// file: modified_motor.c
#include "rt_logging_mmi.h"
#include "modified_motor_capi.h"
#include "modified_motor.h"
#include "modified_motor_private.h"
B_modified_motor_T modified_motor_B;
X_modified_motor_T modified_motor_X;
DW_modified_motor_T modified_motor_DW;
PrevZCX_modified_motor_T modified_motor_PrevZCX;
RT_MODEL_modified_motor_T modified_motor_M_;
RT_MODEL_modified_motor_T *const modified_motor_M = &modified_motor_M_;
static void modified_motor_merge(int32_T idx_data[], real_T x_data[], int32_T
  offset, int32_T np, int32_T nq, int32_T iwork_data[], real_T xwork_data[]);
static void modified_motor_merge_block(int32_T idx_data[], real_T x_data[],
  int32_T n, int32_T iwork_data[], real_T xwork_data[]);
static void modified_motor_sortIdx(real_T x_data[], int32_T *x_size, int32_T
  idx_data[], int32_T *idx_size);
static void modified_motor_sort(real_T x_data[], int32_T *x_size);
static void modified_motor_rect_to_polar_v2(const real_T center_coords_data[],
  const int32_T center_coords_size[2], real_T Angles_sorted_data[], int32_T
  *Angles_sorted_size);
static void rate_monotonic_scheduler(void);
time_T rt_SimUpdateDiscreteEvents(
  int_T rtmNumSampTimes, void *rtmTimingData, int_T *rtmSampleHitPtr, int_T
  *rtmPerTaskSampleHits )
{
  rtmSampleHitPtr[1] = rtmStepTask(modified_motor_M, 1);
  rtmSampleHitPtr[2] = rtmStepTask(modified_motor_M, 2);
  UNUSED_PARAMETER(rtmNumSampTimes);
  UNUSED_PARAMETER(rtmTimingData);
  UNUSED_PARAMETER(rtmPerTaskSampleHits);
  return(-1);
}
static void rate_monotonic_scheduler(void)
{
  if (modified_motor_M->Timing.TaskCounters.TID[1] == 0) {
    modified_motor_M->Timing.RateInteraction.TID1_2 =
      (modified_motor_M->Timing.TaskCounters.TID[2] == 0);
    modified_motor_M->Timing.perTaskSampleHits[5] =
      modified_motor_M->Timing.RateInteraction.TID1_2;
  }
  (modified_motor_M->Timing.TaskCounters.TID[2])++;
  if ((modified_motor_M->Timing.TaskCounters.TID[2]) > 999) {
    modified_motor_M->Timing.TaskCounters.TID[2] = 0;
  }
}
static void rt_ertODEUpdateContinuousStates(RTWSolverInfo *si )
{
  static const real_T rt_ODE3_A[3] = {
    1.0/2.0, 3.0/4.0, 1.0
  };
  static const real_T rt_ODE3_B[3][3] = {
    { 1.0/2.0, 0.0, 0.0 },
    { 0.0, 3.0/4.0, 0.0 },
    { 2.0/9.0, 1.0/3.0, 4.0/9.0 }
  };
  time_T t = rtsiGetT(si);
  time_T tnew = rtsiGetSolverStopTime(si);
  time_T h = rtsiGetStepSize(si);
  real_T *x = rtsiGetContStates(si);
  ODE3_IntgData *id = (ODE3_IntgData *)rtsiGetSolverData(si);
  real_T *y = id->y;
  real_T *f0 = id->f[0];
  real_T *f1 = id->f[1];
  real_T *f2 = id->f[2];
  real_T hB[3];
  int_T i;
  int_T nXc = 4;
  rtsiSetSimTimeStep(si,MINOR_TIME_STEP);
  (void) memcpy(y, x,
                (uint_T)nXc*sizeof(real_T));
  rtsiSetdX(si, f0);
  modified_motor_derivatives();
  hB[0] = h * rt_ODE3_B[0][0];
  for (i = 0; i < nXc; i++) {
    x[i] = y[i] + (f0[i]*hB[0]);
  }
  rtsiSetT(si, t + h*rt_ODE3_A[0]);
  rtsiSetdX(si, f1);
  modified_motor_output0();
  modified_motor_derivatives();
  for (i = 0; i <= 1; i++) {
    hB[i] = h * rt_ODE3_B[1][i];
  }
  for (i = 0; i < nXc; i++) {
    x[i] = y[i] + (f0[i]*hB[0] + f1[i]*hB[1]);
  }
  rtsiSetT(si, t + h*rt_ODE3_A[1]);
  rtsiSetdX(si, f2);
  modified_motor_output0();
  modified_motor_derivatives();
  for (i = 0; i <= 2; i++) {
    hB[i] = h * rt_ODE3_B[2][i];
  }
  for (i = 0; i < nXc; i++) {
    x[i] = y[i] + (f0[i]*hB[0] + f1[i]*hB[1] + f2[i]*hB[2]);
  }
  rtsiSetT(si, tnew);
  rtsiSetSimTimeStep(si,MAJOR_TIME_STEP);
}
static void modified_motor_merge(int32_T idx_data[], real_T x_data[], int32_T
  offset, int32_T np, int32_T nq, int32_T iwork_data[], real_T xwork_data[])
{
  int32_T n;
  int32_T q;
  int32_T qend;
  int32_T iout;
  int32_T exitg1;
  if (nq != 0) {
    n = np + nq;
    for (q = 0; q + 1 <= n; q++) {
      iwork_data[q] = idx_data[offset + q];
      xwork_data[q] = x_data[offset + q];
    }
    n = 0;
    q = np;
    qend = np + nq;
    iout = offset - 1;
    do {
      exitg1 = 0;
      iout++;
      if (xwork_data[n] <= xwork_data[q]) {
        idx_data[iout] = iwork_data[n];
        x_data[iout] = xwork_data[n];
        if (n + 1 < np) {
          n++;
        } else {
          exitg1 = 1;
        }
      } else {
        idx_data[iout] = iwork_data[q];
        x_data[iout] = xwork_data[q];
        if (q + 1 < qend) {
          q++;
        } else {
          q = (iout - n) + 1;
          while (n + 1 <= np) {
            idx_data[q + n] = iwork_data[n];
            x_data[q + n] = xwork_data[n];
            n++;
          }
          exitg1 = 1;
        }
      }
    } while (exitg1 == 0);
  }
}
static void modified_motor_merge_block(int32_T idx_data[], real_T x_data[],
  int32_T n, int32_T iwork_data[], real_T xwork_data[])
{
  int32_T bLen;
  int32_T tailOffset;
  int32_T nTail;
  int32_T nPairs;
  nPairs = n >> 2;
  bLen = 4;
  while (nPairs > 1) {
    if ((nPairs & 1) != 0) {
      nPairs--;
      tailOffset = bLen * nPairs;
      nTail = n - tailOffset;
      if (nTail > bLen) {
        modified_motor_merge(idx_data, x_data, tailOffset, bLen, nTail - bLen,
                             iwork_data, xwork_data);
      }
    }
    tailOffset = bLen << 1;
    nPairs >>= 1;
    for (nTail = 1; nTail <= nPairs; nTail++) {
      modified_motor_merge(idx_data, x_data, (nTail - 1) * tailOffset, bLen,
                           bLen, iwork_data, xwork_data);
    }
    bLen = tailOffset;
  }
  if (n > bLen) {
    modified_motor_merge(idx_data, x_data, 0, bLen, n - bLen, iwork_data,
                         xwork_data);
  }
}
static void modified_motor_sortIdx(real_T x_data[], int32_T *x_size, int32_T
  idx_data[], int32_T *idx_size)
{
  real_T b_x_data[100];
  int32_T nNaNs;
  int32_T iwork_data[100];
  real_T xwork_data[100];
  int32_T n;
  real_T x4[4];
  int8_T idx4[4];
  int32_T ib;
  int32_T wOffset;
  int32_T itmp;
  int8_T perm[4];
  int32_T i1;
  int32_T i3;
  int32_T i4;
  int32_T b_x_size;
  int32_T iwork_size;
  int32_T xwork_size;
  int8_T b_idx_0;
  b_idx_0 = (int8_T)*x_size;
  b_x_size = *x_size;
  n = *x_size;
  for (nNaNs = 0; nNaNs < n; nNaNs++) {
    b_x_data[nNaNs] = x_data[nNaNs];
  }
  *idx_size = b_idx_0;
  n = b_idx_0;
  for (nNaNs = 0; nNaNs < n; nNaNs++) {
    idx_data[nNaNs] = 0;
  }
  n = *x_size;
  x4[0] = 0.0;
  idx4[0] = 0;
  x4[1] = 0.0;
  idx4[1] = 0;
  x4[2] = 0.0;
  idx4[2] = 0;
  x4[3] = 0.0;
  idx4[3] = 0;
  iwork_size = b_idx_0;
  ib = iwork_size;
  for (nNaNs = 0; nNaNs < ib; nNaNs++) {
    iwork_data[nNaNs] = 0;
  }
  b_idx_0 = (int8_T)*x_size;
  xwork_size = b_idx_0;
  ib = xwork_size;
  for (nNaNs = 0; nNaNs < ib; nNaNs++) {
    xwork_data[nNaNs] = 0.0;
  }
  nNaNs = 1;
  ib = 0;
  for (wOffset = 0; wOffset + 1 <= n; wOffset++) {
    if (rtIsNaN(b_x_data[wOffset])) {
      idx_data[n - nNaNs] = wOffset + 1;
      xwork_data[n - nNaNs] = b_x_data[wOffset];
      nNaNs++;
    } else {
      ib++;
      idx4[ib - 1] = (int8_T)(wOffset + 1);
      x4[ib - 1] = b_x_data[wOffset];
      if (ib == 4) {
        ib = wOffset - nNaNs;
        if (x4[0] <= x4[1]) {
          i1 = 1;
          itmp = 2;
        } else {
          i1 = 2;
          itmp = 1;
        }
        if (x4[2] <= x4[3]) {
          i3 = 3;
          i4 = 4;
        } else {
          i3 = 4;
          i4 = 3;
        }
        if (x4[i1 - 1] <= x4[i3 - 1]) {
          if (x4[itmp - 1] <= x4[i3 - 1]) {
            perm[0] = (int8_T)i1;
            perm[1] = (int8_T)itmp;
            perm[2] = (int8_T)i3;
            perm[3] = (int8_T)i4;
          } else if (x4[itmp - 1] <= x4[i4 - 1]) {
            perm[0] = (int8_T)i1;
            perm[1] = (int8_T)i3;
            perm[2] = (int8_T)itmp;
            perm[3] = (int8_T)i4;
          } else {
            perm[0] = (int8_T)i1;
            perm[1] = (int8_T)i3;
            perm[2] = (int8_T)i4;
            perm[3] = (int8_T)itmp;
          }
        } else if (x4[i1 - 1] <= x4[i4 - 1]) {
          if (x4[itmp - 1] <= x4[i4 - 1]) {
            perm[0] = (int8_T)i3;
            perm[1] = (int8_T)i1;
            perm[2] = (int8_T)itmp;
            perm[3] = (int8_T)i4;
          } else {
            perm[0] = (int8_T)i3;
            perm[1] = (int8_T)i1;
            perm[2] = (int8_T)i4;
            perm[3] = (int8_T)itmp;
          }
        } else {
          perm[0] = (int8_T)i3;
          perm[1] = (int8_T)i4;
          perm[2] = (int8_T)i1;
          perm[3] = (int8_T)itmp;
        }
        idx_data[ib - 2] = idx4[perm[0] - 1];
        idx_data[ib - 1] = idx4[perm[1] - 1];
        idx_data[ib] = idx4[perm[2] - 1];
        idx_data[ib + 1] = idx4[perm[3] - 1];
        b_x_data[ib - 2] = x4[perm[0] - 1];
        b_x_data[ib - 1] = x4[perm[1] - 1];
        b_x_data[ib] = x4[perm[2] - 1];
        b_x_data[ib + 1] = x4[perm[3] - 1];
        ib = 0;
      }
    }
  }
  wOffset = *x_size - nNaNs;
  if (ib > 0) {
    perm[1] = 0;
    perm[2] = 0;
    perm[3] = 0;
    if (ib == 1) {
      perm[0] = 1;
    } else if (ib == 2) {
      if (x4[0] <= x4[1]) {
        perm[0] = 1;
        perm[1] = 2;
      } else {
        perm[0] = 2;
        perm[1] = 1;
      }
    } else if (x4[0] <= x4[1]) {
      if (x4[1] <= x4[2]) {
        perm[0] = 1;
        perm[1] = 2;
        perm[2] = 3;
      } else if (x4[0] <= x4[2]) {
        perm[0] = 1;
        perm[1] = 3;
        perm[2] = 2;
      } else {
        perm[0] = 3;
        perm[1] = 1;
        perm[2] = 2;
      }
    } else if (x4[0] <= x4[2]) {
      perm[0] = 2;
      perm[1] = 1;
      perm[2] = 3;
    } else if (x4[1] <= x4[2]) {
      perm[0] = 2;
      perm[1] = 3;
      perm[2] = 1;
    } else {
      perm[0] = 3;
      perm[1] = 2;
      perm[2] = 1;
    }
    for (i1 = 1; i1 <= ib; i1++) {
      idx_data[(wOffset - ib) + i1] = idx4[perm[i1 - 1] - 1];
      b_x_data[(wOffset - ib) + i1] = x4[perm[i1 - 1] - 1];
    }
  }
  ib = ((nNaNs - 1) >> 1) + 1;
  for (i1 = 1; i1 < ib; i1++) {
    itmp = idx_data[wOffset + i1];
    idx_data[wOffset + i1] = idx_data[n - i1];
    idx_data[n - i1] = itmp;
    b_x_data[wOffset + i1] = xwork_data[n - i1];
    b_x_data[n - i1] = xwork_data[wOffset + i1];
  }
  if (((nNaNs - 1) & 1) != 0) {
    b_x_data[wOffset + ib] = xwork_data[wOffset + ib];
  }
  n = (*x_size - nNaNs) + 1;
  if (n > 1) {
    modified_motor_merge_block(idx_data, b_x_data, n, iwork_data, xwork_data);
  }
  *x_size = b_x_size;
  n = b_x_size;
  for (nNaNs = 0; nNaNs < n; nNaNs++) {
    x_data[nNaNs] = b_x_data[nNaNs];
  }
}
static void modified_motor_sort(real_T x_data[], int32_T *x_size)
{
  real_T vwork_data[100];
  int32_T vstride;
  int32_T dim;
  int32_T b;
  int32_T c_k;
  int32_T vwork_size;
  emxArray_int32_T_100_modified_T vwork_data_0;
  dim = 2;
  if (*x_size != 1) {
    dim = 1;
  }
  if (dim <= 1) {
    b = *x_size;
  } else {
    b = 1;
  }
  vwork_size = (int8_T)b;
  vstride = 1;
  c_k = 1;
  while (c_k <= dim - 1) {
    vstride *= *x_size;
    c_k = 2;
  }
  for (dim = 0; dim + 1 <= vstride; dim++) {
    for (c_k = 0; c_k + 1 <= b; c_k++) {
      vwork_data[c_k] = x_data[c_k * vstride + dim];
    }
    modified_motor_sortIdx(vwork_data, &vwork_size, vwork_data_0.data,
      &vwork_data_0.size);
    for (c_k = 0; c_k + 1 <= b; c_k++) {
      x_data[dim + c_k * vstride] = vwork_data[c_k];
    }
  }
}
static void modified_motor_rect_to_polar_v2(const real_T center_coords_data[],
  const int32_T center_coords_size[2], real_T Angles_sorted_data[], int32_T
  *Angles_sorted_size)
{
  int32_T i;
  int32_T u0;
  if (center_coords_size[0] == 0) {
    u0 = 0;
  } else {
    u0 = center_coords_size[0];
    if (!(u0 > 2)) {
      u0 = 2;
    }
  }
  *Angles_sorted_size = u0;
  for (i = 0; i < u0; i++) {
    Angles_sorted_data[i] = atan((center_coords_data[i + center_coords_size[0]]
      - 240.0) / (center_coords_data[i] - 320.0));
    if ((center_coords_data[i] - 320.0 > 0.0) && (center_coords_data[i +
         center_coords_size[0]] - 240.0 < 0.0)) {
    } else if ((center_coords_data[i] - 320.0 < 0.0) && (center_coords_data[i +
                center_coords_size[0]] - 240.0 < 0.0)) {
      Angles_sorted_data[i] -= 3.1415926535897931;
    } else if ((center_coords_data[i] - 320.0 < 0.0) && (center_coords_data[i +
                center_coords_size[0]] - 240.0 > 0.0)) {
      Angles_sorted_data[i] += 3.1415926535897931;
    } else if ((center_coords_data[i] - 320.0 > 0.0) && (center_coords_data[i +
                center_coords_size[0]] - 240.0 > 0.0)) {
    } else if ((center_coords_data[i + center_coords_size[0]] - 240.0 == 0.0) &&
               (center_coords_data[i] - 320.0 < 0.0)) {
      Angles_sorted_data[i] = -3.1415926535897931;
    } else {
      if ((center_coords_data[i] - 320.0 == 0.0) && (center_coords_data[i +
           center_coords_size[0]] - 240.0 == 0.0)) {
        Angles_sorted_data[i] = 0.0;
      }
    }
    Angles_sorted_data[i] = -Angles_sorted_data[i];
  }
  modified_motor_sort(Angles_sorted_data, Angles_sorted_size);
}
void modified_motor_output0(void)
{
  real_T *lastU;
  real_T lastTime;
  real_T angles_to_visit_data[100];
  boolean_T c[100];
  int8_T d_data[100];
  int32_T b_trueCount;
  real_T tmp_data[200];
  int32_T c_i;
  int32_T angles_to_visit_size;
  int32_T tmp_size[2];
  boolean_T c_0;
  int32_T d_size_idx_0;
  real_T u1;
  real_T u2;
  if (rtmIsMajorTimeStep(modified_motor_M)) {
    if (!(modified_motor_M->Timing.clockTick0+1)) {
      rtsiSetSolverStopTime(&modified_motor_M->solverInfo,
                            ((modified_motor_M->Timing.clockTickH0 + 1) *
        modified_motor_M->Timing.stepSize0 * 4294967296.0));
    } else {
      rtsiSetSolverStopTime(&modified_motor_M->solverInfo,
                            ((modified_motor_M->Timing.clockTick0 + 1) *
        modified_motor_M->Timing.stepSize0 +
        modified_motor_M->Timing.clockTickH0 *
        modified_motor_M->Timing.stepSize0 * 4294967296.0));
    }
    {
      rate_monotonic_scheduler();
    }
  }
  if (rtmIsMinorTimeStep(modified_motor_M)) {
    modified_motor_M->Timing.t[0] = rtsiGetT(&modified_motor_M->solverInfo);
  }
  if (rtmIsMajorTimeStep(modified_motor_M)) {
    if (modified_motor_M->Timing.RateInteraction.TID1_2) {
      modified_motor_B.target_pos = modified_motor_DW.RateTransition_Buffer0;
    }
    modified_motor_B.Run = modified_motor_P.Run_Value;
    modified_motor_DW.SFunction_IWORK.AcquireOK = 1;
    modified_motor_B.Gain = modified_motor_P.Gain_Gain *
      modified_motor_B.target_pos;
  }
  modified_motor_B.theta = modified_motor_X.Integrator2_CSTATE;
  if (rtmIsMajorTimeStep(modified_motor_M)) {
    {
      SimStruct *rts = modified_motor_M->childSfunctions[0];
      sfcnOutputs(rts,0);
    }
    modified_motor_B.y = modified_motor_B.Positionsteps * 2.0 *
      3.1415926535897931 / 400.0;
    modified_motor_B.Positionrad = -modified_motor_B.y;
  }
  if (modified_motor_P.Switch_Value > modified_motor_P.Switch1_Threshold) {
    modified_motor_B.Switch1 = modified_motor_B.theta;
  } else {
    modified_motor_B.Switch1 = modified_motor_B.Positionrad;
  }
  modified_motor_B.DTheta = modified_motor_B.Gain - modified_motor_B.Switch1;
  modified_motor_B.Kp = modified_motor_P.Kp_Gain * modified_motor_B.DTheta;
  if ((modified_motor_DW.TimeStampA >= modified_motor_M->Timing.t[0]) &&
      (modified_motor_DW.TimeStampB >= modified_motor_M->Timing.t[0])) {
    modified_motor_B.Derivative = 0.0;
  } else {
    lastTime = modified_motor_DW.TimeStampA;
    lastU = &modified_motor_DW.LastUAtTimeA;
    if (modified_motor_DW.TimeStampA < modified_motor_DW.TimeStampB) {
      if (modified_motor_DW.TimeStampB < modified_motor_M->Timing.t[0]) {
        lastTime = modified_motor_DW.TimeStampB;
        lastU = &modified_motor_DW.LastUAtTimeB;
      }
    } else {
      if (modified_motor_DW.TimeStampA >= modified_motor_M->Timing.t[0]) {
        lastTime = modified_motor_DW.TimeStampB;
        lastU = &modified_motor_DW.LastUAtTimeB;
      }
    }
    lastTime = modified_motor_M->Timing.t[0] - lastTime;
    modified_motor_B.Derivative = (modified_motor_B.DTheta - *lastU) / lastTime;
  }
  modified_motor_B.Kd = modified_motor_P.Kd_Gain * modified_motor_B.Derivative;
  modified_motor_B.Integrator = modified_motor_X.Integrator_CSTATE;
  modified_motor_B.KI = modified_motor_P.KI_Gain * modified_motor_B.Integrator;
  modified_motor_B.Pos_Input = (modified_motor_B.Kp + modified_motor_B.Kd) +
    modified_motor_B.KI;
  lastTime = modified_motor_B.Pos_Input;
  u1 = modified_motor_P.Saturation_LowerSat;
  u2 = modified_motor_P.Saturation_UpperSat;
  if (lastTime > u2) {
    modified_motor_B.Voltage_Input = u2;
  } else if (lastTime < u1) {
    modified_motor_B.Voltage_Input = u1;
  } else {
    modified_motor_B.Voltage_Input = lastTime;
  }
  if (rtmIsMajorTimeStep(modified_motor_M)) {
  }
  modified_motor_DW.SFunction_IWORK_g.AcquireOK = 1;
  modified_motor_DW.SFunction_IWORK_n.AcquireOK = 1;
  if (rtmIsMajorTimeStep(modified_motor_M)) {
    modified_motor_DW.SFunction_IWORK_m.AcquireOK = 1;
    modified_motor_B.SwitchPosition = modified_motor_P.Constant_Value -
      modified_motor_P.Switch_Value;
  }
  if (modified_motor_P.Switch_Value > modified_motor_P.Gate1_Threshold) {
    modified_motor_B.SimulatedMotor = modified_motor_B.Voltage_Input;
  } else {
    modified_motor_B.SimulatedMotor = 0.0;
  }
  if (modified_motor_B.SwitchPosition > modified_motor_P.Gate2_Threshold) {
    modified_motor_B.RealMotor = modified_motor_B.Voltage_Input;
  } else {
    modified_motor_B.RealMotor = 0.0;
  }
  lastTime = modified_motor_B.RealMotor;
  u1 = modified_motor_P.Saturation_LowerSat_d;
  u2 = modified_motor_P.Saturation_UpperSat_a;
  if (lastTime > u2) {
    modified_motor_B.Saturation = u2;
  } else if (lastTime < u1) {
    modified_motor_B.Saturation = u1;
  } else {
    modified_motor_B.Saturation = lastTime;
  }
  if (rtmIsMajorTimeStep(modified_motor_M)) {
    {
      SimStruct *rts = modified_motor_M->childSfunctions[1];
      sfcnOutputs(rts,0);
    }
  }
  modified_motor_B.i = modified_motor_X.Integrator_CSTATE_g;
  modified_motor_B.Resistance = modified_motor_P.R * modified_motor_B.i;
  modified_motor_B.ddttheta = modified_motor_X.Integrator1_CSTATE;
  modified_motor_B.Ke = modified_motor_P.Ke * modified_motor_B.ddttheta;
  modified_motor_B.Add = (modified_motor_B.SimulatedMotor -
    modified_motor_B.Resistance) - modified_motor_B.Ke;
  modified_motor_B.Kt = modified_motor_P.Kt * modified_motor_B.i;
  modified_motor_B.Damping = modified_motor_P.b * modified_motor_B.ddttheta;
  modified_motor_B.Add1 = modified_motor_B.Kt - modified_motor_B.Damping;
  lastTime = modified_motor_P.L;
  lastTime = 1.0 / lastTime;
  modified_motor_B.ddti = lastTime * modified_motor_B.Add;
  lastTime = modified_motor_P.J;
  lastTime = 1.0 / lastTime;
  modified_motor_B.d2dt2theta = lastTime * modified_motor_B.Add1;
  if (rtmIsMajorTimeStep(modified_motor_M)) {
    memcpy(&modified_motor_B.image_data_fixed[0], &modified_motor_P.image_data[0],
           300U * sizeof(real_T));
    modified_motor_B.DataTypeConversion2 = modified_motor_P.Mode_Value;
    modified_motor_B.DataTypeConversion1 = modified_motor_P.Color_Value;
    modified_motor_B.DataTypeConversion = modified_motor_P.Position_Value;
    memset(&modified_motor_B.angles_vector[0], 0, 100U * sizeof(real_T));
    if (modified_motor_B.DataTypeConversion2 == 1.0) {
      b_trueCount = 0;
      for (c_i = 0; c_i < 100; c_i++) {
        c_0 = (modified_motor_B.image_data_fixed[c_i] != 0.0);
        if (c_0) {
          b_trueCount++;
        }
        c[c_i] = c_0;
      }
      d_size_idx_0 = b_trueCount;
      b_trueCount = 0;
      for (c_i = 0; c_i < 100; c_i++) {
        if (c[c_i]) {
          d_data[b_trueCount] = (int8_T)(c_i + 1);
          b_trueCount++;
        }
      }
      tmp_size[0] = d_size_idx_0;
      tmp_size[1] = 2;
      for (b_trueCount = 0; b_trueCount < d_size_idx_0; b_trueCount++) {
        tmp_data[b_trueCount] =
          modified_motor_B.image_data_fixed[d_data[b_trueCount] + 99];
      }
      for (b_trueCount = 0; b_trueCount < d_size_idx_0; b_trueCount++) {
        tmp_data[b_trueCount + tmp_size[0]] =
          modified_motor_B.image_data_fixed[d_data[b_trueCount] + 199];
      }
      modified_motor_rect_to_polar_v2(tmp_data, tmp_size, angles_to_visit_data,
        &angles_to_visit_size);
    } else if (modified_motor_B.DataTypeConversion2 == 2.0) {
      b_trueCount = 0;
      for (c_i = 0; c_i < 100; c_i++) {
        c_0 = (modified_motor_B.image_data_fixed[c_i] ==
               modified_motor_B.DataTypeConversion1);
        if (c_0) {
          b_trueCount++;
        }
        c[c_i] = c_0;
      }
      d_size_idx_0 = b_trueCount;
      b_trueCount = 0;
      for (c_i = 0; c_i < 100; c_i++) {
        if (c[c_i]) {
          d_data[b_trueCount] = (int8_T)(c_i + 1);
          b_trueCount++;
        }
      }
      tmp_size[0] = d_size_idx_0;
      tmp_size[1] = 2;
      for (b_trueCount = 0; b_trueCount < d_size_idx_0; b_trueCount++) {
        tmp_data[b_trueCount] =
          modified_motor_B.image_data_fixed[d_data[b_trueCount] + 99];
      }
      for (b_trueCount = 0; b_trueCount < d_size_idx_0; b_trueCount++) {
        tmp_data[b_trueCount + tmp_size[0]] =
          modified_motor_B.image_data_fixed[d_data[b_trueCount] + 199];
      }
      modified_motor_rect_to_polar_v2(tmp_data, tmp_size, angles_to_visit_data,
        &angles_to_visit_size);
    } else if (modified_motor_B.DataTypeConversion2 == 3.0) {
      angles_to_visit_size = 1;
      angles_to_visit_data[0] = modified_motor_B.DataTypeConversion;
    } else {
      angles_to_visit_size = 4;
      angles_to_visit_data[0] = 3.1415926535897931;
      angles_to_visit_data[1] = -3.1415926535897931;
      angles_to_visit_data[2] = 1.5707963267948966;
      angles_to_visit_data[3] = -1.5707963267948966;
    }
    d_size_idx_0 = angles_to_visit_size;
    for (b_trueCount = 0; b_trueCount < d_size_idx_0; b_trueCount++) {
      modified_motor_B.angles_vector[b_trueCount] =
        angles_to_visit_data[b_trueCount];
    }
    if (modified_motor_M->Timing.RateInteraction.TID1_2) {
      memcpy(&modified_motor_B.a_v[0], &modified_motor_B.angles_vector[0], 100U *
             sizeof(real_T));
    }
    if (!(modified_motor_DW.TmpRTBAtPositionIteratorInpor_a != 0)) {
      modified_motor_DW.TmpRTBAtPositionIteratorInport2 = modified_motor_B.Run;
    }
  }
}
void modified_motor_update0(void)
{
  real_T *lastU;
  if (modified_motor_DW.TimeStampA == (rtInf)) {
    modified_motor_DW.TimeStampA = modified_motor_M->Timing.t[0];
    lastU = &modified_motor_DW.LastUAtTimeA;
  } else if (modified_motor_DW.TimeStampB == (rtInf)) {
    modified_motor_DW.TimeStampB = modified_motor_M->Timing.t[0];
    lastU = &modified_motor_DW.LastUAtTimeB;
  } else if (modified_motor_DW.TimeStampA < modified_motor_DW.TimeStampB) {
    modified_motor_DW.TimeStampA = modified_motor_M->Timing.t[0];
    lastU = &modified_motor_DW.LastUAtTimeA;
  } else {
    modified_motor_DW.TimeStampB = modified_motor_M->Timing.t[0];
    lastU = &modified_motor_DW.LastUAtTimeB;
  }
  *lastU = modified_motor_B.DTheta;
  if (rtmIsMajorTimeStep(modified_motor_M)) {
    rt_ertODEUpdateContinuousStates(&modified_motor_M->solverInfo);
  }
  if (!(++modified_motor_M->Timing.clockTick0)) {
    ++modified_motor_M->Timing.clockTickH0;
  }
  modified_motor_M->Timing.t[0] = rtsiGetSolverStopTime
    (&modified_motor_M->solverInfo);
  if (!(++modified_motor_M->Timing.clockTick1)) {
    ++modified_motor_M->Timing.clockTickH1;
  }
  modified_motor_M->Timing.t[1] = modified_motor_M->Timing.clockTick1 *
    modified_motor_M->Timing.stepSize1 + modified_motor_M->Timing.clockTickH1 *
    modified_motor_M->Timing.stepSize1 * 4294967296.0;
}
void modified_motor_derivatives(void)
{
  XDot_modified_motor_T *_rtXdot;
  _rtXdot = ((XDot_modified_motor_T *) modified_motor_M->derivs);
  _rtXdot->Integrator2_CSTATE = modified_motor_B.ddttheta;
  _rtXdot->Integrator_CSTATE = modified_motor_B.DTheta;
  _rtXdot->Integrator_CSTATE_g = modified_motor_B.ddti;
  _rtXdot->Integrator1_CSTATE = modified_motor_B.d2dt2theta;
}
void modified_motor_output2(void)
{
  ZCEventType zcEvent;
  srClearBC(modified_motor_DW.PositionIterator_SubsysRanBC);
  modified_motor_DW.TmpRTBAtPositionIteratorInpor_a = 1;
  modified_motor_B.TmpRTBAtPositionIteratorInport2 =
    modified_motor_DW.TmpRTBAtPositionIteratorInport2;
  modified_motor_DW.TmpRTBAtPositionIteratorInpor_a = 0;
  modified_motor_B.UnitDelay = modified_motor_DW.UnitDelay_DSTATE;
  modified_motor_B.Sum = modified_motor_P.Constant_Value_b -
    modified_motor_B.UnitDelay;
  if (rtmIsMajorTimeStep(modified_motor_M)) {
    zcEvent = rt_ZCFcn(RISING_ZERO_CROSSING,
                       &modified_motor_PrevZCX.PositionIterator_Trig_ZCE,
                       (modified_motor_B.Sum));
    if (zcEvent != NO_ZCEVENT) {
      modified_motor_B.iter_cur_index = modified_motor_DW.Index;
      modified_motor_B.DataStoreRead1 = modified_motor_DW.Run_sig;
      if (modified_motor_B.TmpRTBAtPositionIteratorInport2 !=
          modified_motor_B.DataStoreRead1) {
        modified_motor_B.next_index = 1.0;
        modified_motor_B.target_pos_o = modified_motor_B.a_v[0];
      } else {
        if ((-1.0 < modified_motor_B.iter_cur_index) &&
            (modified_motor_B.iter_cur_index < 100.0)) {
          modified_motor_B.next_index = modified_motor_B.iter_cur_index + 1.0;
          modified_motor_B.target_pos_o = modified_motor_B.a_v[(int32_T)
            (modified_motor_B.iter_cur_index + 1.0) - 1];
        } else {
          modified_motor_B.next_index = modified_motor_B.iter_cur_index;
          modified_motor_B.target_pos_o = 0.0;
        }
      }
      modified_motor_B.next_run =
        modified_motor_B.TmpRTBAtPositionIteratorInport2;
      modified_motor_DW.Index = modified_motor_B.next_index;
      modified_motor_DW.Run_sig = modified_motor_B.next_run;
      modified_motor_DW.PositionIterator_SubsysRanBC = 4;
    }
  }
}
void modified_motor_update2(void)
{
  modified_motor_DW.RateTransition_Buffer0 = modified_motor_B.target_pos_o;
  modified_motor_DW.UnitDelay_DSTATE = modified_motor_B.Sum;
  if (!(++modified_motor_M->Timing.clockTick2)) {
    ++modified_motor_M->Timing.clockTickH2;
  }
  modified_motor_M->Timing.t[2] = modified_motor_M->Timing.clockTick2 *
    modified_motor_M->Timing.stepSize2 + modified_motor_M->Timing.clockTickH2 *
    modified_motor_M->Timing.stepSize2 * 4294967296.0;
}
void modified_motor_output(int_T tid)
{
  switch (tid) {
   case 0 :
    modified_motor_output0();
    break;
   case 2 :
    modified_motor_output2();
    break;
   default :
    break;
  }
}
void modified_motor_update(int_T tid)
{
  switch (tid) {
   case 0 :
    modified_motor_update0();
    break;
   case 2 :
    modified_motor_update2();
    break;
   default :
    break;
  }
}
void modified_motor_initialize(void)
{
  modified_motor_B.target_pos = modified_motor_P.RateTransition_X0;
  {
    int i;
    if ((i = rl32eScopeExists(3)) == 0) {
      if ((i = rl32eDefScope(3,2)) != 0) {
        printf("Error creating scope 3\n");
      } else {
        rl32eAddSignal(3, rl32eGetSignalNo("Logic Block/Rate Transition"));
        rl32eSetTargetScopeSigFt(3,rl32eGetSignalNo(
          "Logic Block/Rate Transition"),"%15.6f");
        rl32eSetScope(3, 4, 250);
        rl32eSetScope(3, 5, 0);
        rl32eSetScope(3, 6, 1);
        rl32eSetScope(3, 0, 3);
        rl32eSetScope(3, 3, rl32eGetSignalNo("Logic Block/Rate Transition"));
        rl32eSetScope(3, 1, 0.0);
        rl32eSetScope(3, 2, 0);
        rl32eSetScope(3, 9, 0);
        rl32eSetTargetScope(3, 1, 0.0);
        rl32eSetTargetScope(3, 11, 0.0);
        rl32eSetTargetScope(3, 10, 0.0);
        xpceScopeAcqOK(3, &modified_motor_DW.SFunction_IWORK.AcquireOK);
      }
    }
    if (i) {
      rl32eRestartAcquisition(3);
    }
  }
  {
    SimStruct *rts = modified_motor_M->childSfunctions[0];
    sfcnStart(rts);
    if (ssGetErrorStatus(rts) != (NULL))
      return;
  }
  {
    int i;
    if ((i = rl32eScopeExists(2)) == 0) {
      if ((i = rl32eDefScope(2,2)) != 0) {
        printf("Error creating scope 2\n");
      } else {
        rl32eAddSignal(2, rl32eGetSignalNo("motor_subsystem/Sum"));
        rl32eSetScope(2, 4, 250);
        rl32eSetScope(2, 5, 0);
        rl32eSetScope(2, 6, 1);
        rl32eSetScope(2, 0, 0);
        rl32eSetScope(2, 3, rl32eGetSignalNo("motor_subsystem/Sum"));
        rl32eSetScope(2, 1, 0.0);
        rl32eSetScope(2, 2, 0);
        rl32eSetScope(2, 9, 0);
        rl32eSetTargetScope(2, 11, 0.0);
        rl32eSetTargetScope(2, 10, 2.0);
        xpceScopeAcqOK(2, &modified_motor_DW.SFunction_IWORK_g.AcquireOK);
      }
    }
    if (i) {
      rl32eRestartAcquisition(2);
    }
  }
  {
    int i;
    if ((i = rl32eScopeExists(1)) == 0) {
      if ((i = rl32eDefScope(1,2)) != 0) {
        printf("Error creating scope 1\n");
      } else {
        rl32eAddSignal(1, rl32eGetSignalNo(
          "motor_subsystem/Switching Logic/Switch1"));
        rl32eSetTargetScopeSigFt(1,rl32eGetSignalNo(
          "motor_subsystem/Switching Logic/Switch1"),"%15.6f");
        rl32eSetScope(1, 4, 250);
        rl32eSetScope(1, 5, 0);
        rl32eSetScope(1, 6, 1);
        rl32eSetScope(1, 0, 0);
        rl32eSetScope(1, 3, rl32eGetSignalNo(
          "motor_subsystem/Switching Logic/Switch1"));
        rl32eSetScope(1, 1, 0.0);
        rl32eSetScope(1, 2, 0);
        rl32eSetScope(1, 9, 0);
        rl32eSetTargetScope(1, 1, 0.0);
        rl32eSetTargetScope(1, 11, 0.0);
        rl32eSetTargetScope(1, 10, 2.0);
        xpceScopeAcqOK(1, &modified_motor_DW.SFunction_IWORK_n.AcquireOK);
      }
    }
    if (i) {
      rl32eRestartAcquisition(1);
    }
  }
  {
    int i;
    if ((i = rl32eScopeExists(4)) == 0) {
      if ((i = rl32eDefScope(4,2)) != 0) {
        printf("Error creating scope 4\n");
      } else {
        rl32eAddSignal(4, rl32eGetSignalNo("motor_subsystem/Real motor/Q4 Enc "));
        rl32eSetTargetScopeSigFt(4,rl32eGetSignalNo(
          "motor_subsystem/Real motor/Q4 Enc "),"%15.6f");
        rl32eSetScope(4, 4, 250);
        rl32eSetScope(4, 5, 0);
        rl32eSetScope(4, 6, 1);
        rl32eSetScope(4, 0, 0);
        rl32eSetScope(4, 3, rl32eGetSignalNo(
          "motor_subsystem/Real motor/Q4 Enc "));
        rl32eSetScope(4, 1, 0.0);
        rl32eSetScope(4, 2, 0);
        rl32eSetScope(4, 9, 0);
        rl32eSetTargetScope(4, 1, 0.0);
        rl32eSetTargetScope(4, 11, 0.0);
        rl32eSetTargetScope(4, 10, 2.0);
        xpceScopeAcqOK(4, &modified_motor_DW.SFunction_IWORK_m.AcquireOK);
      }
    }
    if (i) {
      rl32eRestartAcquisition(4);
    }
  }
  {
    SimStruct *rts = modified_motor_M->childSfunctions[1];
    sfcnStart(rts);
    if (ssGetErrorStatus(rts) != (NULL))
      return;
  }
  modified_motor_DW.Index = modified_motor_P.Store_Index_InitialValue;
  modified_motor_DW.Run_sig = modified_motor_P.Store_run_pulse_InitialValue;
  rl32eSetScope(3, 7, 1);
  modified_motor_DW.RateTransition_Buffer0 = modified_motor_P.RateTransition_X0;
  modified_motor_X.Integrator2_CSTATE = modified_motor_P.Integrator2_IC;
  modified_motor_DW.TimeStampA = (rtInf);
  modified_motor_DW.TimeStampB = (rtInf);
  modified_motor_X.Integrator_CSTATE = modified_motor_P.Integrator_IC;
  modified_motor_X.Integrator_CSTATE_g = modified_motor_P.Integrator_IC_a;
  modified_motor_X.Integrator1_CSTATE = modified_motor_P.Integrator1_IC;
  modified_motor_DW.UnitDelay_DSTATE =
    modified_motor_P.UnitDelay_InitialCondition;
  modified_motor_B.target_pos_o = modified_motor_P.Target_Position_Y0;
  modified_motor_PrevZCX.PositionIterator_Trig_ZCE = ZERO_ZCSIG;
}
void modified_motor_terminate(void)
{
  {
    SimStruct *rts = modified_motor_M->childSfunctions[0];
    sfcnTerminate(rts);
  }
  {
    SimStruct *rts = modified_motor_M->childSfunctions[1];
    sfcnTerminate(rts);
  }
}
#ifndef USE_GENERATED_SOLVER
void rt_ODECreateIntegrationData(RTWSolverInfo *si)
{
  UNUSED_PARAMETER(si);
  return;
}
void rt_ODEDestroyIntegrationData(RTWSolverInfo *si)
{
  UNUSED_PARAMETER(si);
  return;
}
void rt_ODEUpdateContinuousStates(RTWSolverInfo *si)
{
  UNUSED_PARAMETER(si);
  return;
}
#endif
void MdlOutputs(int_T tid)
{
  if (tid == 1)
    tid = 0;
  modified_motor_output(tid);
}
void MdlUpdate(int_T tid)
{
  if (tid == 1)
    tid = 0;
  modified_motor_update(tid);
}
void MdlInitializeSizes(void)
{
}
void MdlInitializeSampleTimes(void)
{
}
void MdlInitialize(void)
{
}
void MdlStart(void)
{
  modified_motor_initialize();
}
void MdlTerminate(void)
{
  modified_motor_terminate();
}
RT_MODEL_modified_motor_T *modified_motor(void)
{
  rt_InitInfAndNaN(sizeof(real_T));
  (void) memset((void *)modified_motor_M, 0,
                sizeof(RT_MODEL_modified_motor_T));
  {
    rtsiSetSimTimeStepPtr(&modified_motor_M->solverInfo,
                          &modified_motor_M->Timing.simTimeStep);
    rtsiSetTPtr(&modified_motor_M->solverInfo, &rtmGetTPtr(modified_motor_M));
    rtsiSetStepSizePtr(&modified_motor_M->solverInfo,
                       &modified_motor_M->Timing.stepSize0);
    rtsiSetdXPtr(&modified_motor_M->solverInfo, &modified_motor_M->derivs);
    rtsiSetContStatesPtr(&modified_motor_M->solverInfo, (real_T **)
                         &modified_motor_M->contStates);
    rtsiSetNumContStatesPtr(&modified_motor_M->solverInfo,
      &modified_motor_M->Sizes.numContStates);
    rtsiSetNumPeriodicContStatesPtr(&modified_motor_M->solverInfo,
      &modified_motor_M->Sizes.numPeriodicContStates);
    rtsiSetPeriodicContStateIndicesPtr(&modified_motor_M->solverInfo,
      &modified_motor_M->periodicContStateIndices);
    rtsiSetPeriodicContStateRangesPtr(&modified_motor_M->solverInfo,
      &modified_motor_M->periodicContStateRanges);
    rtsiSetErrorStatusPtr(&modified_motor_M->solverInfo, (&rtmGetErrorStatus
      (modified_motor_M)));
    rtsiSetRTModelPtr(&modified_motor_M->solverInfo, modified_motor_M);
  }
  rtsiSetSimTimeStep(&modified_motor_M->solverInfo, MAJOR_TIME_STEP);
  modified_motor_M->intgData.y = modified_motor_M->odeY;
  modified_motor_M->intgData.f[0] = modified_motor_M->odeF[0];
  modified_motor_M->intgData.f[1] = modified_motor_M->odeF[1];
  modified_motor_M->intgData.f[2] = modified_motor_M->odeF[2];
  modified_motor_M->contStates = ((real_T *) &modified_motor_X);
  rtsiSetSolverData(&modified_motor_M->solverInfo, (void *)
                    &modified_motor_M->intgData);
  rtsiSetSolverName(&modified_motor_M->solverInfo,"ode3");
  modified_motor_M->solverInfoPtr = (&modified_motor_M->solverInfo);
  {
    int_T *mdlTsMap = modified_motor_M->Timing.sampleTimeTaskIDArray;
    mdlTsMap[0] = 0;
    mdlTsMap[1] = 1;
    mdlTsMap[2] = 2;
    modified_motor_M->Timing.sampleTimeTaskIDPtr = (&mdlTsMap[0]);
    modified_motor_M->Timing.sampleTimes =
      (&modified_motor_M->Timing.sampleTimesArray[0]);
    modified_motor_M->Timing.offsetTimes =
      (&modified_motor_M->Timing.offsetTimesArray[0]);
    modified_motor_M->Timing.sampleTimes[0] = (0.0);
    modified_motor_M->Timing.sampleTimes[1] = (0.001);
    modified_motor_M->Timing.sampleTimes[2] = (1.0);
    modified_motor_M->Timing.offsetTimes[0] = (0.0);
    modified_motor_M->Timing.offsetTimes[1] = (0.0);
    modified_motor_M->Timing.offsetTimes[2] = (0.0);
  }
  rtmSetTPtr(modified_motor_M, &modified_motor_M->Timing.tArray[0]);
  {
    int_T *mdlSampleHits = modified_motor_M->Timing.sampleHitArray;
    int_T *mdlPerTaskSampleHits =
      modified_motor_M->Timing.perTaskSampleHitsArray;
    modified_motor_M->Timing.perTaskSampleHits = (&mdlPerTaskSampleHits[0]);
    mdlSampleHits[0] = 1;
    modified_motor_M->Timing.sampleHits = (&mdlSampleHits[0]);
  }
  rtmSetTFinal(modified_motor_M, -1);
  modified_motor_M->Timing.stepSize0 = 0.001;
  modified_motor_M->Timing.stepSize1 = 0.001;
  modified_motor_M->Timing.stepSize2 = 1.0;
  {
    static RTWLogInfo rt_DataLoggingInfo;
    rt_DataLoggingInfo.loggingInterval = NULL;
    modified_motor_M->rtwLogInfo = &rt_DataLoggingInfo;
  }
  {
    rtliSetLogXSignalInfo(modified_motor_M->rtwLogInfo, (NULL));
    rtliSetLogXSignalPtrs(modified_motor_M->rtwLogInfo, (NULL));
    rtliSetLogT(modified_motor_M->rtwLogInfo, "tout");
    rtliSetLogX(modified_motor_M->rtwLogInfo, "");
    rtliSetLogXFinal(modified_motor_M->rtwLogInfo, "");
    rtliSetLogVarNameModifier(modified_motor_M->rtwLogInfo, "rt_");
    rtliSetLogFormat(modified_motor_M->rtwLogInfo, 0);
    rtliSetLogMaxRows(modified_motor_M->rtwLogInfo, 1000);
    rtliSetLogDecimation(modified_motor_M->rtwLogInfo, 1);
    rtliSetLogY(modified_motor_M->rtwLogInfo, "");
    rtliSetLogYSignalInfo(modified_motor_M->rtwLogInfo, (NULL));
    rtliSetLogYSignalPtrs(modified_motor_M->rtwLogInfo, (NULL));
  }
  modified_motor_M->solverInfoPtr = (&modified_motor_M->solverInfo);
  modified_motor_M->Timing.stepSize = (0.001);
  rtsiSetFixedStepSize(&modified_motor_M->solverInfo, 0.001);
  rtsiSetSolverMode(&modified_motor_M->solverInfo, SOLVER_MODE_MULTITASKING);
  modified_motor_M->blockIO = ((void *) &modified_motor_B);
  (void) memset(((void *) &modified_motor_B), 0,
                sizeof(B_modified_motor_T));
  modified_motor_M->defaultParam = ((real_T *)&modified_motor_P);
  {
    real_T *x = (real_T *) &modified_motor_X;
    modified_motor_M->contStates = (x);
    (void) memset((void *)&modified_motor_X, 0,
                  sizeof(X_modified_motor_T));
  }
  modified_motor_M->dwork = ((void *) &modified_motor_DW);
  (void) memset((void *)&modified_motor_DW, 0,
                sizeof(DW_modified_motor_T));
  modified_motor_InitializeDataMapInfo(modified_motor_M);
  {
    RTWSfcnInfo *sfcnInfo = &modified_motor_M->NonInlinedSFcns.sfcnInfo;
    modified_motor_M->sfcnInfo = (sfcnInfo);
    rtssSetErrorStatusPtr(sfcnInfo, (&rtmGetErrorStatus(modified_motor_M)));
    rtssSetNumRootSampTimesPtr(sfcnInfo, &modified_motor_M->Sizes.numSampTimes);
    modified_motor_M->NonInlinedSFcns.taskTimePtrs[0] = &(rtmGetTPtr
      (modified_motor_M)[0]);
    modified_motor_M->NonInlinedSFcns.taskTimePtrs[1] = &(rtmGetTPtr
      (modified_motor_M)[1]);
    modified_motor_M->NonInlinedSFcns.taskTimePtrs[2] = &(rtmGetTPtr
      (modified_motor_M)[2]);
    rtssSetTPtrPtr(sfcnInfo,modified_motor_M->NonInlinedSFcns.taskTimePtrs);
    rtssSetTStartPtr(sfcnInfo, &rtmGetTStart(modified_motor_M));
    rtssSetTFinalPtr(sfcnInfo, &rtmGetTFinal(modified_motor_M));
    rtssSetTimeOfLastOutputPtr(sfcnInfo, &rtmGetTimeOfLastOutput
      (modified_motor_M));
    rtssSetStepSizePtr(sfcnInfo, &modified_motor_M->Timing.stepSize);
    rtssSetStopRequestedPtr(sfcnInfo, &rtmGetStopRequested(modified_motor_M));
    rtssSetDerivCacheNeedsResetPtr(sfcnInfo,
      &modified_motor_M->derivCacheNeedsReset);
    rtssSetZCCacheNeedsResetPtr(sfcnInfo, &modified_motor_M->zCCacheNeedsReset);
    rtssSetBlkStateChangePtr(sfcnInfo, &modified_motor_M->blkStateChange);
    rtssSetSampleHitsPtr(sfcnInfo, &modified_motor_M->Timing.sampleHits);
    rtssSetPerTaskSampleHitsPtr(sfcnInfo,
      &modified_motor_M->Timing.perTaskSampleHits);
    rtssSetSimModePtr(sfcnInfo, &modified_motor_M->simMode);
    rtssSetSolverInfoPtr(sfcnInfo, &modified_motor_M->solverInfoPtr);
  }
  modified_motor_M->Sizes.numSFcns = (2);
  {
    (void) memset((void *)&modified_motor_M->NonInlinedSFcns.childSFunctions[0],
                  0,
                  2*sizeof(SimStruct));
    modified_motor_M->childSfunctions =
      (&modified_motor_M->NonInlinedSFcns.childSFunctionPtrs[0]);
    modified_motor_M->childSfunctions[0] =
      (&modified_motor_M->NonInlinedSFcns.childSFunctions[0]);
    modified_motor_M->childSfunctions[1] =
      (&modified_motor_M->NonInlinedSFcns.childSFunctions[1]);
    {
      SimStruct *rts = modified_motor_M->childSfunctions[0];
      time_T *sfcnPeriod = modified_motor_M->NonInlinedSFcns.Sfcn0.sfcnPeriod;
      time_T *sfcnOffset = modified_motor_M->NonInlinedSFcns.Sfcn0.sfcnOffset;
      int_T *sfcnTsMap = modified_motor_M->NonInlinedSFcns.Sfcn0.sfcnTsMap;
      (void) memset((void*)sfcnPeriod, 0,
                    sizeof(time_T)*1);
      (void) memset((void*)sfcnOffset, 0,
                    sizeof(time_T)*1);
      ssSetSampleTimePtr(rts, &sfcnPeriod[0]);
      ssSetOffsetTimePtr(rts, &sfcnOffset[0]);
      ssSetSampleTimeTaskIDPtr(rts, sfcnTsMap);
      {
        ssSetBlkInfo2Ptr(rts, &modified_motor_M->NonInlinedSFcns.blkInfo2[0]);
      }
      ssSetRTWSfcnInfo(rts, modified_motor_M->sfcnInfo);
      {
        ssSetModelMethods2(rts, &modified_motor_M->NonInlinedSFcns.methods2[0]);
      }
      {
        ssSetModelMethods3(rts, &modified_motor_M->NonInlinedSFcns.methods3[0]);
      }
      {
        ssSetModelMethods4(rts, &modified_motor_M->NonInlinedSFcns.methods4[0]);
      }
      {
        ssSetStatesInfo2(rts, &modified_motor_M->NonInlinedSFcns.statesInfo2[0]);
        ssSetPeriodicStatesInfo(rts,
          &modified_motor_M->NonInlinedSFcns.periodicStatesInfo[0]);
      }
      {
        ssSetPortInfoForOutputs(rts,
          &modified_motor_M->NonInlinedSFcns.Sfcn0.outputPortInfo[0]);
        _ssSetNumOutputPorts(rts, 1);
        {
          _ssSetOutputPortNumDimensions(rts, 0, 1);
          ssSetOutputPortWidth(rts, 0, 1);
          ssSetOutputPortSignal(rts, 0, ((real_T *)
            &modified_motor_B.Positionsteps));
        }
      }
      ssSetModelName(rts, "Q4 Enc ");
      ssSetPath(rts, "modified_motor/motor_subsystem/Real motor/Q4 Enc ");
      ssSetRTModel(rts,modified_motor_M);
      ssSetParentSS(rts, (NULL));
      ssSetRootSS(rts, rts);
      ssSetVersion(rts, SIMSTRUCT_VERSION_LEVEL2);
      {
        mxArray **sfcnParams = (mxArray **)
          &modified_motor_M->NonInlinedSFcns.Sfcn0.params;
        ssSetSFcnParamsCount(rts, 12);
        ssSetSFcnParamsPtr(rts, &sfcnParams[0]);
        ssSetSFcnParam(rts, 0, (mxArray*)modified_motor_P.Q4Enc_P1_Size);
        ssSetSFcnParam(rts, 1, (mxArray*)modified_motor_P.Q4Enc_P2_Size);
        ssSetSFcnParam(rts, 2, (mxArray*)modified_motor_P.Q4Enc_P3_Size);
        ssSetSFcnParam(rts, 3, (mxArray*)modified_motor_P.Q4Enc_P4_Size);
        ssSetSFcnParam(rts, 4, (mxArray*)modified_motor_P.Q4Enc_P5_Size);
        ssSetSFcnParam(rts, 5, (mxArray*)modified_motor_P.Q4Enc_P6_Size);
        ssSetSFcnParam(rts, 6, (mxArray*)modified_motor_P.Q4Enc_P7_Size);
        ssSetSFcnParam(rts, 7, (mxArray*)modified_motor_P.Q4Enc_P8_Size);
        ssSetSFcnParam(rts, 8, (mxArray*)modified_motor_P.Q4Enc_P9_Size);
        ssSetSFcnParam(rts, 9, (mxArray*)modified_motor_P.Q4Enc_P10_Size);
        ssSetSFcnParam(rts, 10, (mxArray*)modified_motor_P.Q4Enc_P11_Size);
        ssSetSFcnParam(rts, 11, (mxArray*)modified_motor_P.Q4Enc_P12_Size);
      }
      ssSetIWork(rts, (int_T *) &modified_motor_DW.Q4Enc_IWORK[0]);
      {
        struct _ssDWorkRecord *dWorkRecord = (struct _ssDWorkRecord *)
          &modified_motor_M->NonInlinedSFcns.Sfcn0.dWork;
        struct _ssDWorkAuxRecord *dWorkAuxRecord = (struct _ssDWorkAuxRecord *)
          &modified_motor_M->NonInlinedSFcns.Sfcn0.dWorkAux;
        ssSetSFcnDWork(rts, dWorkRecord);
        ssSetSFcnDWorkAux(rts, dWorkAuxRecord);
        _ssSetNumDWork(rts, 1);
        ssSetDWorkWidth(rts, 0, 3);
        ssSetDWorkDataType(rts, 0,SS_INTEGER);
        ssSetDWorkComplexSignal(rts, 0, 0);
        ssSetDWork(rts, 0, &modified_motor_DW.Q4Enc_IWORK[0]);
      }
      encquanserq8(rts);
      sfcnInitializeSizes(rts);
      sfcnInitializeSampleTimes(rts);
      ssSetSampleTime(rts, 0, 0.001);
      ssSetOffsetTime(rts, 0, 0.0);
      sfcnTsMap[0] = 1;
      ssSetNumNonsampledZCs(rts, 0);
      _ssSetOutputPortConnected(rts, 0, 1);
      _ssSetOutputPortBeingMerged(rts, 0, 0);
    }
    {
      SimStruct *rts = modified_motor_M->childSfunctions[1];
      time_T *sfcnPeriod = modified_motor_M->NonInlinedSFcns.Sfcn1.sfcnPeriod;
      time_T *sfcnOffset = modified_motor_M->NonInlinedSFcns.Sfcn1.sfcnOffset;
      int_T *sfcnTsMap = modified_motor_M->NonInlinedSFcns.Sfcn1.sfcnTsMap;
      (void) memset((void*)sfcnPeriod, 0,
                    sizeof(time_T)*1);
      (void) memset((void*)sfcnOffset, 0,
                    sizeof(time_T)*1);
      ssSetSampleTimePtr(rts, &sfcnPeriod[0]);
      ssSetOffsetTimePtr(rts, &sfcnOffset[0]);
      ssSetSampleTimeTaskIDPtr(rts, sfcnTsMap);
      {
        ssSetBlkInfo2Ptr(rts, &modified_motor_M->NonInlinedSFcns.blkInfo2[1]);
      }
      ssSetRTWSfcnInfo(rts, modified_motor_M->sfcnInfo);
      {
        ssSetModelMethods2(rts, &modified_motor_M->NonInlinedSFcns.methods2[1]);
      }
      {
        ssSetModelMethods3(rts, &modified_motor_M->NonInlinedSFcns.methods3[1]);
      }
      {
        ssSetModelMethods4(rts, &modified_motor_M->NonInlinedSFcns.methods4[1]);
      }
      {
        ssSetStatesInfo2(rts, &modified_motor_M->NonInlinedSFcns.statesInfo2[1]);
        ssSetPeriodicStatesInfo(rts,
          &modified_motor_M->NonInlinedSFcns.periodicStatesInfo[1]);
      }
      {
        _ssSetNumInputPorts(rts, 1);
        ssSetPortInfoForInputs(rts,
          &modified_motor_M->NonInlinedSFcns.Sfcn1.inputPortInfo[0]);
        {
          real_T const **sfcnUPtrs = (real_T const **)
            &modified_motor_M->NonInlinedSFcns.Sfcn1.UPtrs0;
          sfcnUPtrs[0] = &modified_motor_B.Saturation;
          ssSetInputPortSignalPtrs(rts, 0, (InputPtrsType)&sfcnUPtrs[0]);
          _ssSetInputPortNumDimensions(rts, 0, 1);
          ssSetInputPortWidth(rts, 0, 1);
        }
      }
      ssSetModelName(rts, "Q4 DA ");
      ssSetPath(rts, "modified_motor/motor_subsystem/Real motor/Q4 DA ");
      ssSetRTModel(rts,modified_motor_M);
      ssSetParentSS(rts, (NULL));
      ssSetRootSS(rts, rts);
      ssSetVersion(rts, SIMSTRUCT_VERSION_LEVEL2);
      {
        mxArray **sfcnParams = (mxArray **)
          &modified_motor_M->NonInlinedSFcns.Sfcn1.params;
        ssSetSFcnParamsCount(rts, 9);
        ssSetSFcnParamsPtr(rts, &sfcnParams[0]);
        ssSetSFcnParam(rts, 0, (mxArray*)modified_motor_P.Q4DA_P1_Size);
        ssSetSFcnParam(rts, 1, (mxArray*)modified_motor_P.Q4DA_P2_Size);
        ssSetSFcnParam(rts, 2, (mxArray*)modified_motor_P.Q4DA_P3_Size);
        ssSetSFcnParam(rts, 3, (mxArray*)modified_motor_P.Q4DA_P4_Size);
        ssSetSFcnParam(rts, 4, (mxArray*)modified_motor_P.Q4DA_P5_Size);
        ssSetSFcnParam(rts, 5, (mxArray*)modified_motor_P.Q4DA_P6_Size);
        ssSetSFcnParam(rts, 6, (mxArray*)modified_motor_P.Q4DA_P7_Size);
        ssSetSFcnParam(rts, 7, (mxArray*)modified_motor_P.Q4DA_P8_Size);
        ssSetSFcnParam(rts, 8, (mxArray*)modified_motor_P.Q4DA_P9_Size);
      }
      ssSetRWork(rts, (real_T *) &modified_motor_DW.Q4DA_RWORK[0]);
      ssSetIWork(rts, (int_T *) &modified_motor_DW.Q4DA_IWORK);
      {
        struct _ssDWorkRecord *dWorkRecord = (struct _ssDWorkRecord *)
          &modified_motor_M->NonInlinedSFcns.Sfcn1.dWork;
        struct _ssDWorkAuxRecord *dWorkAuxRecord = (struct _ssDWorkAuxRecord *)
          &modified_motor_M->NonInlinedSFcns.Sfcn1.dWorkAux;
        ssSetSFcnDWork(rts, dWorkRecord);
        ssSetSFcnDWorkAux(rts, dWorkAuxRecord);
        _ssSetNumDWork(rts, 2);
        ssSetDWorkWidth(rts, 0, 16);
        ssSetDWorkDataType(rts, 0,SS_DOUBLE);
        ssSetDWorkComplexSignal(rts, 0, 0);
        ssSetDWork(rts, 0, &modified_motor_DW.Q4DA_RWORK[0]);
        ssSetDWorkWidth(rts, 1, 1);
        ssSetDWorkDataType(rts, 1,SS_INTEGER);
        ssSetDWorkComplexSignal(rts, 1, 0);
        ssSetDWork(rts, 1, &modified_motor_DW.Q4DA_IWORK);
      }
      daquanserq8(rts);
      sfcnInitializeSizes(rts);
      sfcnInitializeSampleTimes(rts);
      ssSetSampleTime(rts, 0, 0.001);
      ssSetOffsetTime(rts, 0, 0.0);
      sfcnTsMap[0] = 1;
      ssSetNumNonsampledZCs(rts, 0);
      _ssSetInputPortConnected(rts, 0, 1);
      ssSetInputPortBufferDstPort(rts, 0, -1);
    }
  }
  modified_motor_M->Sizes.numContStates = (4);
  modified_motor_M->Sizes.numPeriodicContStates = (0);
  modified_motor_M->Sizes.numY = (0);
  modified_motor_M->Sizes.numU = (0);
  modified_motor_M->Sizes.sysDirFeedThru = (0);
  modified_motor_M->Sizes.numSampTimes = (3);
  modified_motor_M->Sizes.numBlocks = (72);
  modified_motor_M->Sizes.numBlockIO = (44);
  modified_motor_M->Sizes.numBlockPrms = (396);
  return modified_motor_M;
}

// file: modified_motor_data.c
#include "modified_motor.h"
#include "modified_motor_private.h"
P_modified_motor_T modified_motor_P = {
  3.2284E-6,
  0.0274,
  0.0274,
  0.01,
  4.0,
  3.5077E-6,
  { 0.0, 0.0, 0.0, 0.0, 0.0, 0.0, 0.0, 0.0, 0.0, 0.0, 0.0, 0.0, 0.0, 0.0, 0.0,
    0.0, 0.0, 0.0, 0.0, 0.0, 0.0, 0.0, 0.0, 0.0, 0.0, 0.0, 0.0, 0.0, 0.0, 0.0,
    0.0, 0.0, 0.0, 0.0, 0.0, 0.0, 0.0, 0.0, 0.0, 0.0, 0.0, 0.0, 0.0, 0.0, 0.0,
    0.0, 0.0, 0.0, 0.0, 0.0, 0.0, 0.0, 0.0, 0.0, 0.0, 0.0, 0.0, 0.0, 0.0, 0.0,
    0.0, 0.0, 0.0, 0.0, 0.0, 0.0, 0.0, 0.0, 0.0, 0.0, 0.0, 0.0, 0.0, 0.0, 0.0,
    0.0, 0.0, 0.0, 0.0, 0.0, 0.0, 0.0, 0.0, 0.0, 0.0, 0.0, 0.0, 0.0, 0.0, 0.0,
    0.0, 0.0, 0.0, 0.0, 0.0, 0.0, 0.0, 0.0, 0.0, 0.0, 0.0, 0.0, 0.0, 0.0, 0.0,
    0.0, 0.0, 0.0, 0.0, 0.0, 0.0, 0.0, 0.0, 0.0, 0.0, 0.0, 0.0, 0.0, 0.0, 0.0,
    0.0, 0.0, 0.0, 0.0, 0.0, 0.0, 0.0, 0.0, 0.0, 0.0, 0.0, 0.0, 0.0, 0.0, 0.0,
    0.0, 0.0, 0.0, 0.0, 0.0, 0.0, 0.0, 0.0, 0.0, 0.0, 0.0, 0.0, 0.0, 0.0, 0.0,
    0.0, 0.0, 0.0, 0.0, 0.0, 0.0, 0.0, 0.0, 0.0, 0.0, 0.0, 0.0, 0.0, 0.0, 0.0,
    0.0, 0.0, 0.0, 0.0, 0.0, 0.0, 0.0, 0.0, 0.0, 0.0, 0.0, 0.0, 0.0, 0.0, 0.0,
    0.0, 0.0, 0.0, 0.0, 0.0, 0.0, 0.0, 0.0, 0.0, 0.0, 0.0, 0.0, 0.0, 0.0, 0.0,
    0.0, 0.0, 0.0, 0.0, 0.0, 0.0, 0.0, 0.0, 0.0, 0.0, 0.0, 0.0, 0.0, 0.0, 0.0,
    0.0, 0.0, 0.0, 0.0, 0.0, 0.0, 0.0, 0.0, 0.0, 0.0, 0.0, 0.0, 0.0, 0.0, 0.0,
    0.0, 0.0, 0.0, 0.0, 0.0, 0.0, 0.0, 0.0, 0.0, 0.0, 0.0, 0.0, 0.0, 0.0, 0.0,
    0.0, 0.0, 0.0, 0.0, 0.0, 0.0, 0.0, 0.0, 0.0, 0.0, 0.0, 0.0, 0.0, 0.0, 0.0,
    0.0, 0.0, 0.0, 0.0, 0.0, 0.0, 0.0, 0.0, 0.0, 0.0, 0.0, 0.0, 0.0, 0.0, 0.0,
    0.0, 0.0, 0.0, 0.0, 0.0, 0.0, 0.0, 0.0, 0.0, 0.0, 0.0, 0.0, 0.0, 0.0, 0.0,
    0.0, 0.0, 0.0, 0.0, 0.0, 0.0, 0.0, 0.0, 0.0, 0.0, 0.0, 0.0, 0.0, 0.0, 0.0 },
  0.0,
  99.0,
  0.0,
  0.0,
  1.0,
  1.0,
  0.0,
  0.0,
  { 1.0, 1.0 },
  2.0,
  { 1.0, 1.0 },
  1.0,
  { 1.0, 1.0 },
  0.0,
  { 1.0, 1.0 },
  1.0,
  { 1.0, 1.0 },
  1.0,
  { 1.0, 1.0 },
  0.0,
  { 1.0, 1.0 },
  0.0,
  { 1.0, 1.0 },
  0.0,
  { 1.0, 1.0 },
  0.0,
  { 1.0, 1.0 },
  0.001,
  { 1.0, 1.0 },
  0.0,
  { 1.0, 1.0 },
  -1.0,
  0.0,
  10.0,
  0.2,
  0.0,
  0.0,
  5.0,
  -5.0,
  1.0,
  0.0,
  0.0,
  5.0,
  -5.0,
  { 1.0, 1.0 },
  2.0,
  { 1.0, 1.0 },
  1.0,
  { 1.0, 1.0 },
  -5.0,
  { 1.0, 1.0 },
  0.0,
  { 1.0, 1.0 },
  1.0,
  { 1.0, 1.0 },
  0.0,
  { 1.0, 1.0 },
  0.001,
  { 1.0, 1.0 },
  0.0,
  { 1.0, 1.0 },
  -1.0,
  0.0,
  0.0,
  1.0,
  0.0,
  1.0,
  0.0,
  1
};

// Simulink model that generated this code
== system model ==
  Q4DA : xpcquanserlib/D//A/Q4 DA  <- 1: Saturation
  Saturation : Saturate  UpperLimit=5  LowerLimit=-5  <- 1: Gate2
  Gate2 : Switch  Criteria=u2 > Threshold  <- 1: Saturate#1, 2: Add
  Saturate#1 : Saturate  UpperLimit=5  LowerLimit=-5  <- 1: Sum#1
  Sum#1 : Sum  Inputs=+++  <- 1: Kp, 2: Kd, 3: KI
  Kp : Gain  Gain=10  <- 1: Sum
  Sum : Sum  Inputs=+-  <- 1: Gain, 2: Switch1
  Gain : Gain  <- 1: RateTransition
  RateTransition : RateTransition  <- 1: PositionIterator
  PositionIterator : Subsystem  <- 1: RateTransition#1, 2: Run, Trigger: Clock#1
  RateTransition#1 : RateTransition  <- 1: MATLABFunction#1
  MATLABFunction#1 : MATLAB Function  <- 1: DataTypeConversion2, 2: DataTypeConversion1, 3: DataTypeConversion, 4: MATLABFunction#2
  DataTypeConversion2 : DataTypeConversion  <- 1: Mode
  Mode : Constant
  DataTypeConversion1 : DataTypeConversion  <- 1: Color
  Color : Constant
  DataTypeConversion : DataTypeConversion  <- 1: Position
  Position : Constant  Value=0
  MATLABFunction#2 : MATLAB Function  <- 1: Constant
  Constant : Constant  Value=image_data
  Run : Constant
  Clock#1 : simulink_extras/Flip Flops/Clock
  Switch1 : Switch  Criteria=u2 > Threshold  <- 1: Integrator2, 2: Switch, 3: Fcn#1
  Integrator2 : Integrator  <- 1: Integrator1
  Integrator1 : Integrator  <- 1: Gain#1
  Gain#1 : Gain  Gain=1/J  <- 1: Add1
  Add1 : Sum  Inputs=+-  <- 1: Kt, 2: Damping
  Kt : Gain  Gain=Kt  <- 1: Integrator
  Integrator : Integrator  <- 1: Gain#2
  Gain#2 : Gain  Gain=1/L  <- 1: Sum#2
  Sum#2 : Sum  Inputs=-+-  <- 1: Resistance, 2: Gate1, 3: Ke
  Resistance : Gain  Gain=R  <- 1: Integrator
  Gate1 : Switch  Criteria=u2 > Threshold  <- 1: Saturate#1, 2: Switch
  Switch : Constant  Value=0
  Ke : Gain  Gain=Ke  <- 1: Integrator1
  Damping : Gain  Gain=b  <- 1: Integrator1
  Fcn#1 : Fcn  Expr=-u  <- 1: MATLABFunction#3
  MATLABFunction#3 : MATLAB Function  <- 1: Q4Enc
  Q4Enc : xpcquanserlib/Incremental Encoder/Q4 Enc
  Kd : Gain  Gain=0.2  <- 1: Derivative
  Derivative : Derivative  <- 1: Sum
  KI : Gain  Gain=0  <- 1: Integrator#1
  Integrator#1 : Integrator  <- 1: Sum
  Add : Sum  Inputs=-+  <- 1: Switch, 2: Constant#1
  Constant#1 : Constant
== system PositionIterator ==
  Inport#1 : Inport
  Inport#2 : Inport
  TriggerPort#1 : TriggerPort
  Target_Position : Outport  <- 1: MATLABFunction#4
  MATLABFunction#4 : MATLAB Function  <- 1: Inport#1, 2: DataStoreRead#1, 3: Inport#2, 4: DataStoreRead1
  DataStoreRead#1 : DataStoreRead  DataStoreName=Index
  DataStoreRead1 : DataStoreRead  DataStoreName=Run_sig
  DataStoreWrite#1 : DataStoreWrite  DataStoreName=Index  <- 1: MATLABFunction#4/2
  DataStoreWrite#2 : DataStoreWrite  DataStoreName=Run_sig  <- 1: MATLABFunction#4/3
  Store_Index : DataStoreMemory  DataStoreName=Index  InitialValue=99
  Store_run_pulse : DataStoreMemory  DataStoreName=Run_sig
== matlab function MATLABFunction#1 ==
% PURPOSE - Parser to set 
% INPUTS
%   - Mode: What should the system do in response to the user selection
%       - scan: Visit every well with a sticker
%       - seek color: Visit every well with a sticker of the given color
%       - seek position: Visit only the well with the given sticker ID
%   - Color Enum: What color the system should visit
%   - Position: Angle in radians to visit
%   - Image Data: 2D processed data from webcam
%       - Col 1: Color
%       - Col 2: X Position
%       - Col 3: Y Position
% OUTPUTS
%   - positions_to_visit: Vector of fixed destination positions on [-pi, pi) 
%       to which the motor arm should point in sequence.
% NOTES
%   - If mode = 1 then the function ignores requested position and color.
%   - If mode = 2 then the function ignores requested position.
%   - If mode = 3 then the function ignores requested color.

function angles_vector = make_angle_vector(mode, color, position, img_data)

% MATLAB expects a fixed-size output matrix so allow up to 100 angles
% to be propagated
MAX_ANGLES_TO_VISIT = 100;

MODE_SCAN = 1;
MODE_SEEK_COLOR = 2;
MODE_SEEK_POSITION = 3;

COLOR_COL = 1;
X_COL = 2;
Y_COL = 3;

angles_vector = zeros(MAX_ANGLES_TO_VISIT, 1);

if mode == MODE_SCAN
    rect_coords = img_data(img_data(:,1) ~= 0, X_COL:Y_COL);
    angles_to_visit = rect_to_polar_v2(rect_coords);

elseif mode == MODE_SEEK_COLOR
    rect_coords = img_data(img_data(:, COLOR_COL) == color, X_COL:Y_COL);
    angles_to_visit = rect_to_polar_v2(rect_coords);

elseif mode == MODE_SEEK_POSITION
    angles_to_visit = position;

else
    angles_to_visit = [pi; -pi; pi/2; -pi/2];
end

% Package variable-length vector into fixed-length vector
angles_vector(1:size(angles_to_visit,1), :) = angles_to_visit;

== matlab function MATLABFunction#3 ==
function y = fcn(u)

% Observed experimentally
STEPS_IN_ONE_ROTATION = 400;

rads_from_zero_to_twopi = u * 2 * pi / STEPS_IN_ONE_ROTATION;

y = rads_from_zero_to_twopi;

== matlab function MATLABFunction#2 ==
function image_data_fixed = process_image(img)

% Can only send fixed-length matrices so specify max 100 regions
REGIONS_SIGNAL_CAPACITY = 100;

% FIXME do processing
image_data_fixed = zeros(REGIONS_SIGNAL_CAPACITY, 3);

% ex. pass back [shape; color; x_pos; y_pos]
image_data_fixed(1:size(img,1),:) = img;

== matlab function MATLABFunction#4 ==
% PURPOSE - Iterate over list of positions to visit
% INPUTS
%   - Position List: Vector of target positions for the motor to turn to
%   - Current Index: Loopback to store variable state
%   - Clock: Trigger to move to the next position
%   - Reset: Trigger to reset to first position in list (0 == HIGH)
% OUTPUTS
%   - Target Position: Motor position on range [-pi, pi) 
%   - Next Index: Loopback to store variable state
% BEHAVIOR
%   - If Reset is high then reset index to 0 and output first position
%   - Else if Clock is low then output the position at the current index
%   - Else if the index is at the end of the list then output 0
%   - Else increment the index and output the next position

function [target_pos, next_index, next_run] = iterate(pos_list, cur_index, cur_run, last_run)

% PRECONDITION: pos_list is a column vector
assert(size(pos_list, 2) == 1)

ZERO_POSITION = 0;
pos_list_len = size(pos_list, 1);

% This is a very hack-y edge trigger
if cur_run ~= last_run
   next_index = 1;
   target_pos = pos_list(1);
else
   % If we can increment then do that
    if -1 < cur_index && cur_index < pos_list_len
        next_index = cur_index + 1;
        target_pos = pos_list(cur_index + 1);
    % Otherwise maintain current state
    else
        next_index = cur_index;
        target_pos = ZERO_POSITION;
    end
end

next_run = cur_run;
